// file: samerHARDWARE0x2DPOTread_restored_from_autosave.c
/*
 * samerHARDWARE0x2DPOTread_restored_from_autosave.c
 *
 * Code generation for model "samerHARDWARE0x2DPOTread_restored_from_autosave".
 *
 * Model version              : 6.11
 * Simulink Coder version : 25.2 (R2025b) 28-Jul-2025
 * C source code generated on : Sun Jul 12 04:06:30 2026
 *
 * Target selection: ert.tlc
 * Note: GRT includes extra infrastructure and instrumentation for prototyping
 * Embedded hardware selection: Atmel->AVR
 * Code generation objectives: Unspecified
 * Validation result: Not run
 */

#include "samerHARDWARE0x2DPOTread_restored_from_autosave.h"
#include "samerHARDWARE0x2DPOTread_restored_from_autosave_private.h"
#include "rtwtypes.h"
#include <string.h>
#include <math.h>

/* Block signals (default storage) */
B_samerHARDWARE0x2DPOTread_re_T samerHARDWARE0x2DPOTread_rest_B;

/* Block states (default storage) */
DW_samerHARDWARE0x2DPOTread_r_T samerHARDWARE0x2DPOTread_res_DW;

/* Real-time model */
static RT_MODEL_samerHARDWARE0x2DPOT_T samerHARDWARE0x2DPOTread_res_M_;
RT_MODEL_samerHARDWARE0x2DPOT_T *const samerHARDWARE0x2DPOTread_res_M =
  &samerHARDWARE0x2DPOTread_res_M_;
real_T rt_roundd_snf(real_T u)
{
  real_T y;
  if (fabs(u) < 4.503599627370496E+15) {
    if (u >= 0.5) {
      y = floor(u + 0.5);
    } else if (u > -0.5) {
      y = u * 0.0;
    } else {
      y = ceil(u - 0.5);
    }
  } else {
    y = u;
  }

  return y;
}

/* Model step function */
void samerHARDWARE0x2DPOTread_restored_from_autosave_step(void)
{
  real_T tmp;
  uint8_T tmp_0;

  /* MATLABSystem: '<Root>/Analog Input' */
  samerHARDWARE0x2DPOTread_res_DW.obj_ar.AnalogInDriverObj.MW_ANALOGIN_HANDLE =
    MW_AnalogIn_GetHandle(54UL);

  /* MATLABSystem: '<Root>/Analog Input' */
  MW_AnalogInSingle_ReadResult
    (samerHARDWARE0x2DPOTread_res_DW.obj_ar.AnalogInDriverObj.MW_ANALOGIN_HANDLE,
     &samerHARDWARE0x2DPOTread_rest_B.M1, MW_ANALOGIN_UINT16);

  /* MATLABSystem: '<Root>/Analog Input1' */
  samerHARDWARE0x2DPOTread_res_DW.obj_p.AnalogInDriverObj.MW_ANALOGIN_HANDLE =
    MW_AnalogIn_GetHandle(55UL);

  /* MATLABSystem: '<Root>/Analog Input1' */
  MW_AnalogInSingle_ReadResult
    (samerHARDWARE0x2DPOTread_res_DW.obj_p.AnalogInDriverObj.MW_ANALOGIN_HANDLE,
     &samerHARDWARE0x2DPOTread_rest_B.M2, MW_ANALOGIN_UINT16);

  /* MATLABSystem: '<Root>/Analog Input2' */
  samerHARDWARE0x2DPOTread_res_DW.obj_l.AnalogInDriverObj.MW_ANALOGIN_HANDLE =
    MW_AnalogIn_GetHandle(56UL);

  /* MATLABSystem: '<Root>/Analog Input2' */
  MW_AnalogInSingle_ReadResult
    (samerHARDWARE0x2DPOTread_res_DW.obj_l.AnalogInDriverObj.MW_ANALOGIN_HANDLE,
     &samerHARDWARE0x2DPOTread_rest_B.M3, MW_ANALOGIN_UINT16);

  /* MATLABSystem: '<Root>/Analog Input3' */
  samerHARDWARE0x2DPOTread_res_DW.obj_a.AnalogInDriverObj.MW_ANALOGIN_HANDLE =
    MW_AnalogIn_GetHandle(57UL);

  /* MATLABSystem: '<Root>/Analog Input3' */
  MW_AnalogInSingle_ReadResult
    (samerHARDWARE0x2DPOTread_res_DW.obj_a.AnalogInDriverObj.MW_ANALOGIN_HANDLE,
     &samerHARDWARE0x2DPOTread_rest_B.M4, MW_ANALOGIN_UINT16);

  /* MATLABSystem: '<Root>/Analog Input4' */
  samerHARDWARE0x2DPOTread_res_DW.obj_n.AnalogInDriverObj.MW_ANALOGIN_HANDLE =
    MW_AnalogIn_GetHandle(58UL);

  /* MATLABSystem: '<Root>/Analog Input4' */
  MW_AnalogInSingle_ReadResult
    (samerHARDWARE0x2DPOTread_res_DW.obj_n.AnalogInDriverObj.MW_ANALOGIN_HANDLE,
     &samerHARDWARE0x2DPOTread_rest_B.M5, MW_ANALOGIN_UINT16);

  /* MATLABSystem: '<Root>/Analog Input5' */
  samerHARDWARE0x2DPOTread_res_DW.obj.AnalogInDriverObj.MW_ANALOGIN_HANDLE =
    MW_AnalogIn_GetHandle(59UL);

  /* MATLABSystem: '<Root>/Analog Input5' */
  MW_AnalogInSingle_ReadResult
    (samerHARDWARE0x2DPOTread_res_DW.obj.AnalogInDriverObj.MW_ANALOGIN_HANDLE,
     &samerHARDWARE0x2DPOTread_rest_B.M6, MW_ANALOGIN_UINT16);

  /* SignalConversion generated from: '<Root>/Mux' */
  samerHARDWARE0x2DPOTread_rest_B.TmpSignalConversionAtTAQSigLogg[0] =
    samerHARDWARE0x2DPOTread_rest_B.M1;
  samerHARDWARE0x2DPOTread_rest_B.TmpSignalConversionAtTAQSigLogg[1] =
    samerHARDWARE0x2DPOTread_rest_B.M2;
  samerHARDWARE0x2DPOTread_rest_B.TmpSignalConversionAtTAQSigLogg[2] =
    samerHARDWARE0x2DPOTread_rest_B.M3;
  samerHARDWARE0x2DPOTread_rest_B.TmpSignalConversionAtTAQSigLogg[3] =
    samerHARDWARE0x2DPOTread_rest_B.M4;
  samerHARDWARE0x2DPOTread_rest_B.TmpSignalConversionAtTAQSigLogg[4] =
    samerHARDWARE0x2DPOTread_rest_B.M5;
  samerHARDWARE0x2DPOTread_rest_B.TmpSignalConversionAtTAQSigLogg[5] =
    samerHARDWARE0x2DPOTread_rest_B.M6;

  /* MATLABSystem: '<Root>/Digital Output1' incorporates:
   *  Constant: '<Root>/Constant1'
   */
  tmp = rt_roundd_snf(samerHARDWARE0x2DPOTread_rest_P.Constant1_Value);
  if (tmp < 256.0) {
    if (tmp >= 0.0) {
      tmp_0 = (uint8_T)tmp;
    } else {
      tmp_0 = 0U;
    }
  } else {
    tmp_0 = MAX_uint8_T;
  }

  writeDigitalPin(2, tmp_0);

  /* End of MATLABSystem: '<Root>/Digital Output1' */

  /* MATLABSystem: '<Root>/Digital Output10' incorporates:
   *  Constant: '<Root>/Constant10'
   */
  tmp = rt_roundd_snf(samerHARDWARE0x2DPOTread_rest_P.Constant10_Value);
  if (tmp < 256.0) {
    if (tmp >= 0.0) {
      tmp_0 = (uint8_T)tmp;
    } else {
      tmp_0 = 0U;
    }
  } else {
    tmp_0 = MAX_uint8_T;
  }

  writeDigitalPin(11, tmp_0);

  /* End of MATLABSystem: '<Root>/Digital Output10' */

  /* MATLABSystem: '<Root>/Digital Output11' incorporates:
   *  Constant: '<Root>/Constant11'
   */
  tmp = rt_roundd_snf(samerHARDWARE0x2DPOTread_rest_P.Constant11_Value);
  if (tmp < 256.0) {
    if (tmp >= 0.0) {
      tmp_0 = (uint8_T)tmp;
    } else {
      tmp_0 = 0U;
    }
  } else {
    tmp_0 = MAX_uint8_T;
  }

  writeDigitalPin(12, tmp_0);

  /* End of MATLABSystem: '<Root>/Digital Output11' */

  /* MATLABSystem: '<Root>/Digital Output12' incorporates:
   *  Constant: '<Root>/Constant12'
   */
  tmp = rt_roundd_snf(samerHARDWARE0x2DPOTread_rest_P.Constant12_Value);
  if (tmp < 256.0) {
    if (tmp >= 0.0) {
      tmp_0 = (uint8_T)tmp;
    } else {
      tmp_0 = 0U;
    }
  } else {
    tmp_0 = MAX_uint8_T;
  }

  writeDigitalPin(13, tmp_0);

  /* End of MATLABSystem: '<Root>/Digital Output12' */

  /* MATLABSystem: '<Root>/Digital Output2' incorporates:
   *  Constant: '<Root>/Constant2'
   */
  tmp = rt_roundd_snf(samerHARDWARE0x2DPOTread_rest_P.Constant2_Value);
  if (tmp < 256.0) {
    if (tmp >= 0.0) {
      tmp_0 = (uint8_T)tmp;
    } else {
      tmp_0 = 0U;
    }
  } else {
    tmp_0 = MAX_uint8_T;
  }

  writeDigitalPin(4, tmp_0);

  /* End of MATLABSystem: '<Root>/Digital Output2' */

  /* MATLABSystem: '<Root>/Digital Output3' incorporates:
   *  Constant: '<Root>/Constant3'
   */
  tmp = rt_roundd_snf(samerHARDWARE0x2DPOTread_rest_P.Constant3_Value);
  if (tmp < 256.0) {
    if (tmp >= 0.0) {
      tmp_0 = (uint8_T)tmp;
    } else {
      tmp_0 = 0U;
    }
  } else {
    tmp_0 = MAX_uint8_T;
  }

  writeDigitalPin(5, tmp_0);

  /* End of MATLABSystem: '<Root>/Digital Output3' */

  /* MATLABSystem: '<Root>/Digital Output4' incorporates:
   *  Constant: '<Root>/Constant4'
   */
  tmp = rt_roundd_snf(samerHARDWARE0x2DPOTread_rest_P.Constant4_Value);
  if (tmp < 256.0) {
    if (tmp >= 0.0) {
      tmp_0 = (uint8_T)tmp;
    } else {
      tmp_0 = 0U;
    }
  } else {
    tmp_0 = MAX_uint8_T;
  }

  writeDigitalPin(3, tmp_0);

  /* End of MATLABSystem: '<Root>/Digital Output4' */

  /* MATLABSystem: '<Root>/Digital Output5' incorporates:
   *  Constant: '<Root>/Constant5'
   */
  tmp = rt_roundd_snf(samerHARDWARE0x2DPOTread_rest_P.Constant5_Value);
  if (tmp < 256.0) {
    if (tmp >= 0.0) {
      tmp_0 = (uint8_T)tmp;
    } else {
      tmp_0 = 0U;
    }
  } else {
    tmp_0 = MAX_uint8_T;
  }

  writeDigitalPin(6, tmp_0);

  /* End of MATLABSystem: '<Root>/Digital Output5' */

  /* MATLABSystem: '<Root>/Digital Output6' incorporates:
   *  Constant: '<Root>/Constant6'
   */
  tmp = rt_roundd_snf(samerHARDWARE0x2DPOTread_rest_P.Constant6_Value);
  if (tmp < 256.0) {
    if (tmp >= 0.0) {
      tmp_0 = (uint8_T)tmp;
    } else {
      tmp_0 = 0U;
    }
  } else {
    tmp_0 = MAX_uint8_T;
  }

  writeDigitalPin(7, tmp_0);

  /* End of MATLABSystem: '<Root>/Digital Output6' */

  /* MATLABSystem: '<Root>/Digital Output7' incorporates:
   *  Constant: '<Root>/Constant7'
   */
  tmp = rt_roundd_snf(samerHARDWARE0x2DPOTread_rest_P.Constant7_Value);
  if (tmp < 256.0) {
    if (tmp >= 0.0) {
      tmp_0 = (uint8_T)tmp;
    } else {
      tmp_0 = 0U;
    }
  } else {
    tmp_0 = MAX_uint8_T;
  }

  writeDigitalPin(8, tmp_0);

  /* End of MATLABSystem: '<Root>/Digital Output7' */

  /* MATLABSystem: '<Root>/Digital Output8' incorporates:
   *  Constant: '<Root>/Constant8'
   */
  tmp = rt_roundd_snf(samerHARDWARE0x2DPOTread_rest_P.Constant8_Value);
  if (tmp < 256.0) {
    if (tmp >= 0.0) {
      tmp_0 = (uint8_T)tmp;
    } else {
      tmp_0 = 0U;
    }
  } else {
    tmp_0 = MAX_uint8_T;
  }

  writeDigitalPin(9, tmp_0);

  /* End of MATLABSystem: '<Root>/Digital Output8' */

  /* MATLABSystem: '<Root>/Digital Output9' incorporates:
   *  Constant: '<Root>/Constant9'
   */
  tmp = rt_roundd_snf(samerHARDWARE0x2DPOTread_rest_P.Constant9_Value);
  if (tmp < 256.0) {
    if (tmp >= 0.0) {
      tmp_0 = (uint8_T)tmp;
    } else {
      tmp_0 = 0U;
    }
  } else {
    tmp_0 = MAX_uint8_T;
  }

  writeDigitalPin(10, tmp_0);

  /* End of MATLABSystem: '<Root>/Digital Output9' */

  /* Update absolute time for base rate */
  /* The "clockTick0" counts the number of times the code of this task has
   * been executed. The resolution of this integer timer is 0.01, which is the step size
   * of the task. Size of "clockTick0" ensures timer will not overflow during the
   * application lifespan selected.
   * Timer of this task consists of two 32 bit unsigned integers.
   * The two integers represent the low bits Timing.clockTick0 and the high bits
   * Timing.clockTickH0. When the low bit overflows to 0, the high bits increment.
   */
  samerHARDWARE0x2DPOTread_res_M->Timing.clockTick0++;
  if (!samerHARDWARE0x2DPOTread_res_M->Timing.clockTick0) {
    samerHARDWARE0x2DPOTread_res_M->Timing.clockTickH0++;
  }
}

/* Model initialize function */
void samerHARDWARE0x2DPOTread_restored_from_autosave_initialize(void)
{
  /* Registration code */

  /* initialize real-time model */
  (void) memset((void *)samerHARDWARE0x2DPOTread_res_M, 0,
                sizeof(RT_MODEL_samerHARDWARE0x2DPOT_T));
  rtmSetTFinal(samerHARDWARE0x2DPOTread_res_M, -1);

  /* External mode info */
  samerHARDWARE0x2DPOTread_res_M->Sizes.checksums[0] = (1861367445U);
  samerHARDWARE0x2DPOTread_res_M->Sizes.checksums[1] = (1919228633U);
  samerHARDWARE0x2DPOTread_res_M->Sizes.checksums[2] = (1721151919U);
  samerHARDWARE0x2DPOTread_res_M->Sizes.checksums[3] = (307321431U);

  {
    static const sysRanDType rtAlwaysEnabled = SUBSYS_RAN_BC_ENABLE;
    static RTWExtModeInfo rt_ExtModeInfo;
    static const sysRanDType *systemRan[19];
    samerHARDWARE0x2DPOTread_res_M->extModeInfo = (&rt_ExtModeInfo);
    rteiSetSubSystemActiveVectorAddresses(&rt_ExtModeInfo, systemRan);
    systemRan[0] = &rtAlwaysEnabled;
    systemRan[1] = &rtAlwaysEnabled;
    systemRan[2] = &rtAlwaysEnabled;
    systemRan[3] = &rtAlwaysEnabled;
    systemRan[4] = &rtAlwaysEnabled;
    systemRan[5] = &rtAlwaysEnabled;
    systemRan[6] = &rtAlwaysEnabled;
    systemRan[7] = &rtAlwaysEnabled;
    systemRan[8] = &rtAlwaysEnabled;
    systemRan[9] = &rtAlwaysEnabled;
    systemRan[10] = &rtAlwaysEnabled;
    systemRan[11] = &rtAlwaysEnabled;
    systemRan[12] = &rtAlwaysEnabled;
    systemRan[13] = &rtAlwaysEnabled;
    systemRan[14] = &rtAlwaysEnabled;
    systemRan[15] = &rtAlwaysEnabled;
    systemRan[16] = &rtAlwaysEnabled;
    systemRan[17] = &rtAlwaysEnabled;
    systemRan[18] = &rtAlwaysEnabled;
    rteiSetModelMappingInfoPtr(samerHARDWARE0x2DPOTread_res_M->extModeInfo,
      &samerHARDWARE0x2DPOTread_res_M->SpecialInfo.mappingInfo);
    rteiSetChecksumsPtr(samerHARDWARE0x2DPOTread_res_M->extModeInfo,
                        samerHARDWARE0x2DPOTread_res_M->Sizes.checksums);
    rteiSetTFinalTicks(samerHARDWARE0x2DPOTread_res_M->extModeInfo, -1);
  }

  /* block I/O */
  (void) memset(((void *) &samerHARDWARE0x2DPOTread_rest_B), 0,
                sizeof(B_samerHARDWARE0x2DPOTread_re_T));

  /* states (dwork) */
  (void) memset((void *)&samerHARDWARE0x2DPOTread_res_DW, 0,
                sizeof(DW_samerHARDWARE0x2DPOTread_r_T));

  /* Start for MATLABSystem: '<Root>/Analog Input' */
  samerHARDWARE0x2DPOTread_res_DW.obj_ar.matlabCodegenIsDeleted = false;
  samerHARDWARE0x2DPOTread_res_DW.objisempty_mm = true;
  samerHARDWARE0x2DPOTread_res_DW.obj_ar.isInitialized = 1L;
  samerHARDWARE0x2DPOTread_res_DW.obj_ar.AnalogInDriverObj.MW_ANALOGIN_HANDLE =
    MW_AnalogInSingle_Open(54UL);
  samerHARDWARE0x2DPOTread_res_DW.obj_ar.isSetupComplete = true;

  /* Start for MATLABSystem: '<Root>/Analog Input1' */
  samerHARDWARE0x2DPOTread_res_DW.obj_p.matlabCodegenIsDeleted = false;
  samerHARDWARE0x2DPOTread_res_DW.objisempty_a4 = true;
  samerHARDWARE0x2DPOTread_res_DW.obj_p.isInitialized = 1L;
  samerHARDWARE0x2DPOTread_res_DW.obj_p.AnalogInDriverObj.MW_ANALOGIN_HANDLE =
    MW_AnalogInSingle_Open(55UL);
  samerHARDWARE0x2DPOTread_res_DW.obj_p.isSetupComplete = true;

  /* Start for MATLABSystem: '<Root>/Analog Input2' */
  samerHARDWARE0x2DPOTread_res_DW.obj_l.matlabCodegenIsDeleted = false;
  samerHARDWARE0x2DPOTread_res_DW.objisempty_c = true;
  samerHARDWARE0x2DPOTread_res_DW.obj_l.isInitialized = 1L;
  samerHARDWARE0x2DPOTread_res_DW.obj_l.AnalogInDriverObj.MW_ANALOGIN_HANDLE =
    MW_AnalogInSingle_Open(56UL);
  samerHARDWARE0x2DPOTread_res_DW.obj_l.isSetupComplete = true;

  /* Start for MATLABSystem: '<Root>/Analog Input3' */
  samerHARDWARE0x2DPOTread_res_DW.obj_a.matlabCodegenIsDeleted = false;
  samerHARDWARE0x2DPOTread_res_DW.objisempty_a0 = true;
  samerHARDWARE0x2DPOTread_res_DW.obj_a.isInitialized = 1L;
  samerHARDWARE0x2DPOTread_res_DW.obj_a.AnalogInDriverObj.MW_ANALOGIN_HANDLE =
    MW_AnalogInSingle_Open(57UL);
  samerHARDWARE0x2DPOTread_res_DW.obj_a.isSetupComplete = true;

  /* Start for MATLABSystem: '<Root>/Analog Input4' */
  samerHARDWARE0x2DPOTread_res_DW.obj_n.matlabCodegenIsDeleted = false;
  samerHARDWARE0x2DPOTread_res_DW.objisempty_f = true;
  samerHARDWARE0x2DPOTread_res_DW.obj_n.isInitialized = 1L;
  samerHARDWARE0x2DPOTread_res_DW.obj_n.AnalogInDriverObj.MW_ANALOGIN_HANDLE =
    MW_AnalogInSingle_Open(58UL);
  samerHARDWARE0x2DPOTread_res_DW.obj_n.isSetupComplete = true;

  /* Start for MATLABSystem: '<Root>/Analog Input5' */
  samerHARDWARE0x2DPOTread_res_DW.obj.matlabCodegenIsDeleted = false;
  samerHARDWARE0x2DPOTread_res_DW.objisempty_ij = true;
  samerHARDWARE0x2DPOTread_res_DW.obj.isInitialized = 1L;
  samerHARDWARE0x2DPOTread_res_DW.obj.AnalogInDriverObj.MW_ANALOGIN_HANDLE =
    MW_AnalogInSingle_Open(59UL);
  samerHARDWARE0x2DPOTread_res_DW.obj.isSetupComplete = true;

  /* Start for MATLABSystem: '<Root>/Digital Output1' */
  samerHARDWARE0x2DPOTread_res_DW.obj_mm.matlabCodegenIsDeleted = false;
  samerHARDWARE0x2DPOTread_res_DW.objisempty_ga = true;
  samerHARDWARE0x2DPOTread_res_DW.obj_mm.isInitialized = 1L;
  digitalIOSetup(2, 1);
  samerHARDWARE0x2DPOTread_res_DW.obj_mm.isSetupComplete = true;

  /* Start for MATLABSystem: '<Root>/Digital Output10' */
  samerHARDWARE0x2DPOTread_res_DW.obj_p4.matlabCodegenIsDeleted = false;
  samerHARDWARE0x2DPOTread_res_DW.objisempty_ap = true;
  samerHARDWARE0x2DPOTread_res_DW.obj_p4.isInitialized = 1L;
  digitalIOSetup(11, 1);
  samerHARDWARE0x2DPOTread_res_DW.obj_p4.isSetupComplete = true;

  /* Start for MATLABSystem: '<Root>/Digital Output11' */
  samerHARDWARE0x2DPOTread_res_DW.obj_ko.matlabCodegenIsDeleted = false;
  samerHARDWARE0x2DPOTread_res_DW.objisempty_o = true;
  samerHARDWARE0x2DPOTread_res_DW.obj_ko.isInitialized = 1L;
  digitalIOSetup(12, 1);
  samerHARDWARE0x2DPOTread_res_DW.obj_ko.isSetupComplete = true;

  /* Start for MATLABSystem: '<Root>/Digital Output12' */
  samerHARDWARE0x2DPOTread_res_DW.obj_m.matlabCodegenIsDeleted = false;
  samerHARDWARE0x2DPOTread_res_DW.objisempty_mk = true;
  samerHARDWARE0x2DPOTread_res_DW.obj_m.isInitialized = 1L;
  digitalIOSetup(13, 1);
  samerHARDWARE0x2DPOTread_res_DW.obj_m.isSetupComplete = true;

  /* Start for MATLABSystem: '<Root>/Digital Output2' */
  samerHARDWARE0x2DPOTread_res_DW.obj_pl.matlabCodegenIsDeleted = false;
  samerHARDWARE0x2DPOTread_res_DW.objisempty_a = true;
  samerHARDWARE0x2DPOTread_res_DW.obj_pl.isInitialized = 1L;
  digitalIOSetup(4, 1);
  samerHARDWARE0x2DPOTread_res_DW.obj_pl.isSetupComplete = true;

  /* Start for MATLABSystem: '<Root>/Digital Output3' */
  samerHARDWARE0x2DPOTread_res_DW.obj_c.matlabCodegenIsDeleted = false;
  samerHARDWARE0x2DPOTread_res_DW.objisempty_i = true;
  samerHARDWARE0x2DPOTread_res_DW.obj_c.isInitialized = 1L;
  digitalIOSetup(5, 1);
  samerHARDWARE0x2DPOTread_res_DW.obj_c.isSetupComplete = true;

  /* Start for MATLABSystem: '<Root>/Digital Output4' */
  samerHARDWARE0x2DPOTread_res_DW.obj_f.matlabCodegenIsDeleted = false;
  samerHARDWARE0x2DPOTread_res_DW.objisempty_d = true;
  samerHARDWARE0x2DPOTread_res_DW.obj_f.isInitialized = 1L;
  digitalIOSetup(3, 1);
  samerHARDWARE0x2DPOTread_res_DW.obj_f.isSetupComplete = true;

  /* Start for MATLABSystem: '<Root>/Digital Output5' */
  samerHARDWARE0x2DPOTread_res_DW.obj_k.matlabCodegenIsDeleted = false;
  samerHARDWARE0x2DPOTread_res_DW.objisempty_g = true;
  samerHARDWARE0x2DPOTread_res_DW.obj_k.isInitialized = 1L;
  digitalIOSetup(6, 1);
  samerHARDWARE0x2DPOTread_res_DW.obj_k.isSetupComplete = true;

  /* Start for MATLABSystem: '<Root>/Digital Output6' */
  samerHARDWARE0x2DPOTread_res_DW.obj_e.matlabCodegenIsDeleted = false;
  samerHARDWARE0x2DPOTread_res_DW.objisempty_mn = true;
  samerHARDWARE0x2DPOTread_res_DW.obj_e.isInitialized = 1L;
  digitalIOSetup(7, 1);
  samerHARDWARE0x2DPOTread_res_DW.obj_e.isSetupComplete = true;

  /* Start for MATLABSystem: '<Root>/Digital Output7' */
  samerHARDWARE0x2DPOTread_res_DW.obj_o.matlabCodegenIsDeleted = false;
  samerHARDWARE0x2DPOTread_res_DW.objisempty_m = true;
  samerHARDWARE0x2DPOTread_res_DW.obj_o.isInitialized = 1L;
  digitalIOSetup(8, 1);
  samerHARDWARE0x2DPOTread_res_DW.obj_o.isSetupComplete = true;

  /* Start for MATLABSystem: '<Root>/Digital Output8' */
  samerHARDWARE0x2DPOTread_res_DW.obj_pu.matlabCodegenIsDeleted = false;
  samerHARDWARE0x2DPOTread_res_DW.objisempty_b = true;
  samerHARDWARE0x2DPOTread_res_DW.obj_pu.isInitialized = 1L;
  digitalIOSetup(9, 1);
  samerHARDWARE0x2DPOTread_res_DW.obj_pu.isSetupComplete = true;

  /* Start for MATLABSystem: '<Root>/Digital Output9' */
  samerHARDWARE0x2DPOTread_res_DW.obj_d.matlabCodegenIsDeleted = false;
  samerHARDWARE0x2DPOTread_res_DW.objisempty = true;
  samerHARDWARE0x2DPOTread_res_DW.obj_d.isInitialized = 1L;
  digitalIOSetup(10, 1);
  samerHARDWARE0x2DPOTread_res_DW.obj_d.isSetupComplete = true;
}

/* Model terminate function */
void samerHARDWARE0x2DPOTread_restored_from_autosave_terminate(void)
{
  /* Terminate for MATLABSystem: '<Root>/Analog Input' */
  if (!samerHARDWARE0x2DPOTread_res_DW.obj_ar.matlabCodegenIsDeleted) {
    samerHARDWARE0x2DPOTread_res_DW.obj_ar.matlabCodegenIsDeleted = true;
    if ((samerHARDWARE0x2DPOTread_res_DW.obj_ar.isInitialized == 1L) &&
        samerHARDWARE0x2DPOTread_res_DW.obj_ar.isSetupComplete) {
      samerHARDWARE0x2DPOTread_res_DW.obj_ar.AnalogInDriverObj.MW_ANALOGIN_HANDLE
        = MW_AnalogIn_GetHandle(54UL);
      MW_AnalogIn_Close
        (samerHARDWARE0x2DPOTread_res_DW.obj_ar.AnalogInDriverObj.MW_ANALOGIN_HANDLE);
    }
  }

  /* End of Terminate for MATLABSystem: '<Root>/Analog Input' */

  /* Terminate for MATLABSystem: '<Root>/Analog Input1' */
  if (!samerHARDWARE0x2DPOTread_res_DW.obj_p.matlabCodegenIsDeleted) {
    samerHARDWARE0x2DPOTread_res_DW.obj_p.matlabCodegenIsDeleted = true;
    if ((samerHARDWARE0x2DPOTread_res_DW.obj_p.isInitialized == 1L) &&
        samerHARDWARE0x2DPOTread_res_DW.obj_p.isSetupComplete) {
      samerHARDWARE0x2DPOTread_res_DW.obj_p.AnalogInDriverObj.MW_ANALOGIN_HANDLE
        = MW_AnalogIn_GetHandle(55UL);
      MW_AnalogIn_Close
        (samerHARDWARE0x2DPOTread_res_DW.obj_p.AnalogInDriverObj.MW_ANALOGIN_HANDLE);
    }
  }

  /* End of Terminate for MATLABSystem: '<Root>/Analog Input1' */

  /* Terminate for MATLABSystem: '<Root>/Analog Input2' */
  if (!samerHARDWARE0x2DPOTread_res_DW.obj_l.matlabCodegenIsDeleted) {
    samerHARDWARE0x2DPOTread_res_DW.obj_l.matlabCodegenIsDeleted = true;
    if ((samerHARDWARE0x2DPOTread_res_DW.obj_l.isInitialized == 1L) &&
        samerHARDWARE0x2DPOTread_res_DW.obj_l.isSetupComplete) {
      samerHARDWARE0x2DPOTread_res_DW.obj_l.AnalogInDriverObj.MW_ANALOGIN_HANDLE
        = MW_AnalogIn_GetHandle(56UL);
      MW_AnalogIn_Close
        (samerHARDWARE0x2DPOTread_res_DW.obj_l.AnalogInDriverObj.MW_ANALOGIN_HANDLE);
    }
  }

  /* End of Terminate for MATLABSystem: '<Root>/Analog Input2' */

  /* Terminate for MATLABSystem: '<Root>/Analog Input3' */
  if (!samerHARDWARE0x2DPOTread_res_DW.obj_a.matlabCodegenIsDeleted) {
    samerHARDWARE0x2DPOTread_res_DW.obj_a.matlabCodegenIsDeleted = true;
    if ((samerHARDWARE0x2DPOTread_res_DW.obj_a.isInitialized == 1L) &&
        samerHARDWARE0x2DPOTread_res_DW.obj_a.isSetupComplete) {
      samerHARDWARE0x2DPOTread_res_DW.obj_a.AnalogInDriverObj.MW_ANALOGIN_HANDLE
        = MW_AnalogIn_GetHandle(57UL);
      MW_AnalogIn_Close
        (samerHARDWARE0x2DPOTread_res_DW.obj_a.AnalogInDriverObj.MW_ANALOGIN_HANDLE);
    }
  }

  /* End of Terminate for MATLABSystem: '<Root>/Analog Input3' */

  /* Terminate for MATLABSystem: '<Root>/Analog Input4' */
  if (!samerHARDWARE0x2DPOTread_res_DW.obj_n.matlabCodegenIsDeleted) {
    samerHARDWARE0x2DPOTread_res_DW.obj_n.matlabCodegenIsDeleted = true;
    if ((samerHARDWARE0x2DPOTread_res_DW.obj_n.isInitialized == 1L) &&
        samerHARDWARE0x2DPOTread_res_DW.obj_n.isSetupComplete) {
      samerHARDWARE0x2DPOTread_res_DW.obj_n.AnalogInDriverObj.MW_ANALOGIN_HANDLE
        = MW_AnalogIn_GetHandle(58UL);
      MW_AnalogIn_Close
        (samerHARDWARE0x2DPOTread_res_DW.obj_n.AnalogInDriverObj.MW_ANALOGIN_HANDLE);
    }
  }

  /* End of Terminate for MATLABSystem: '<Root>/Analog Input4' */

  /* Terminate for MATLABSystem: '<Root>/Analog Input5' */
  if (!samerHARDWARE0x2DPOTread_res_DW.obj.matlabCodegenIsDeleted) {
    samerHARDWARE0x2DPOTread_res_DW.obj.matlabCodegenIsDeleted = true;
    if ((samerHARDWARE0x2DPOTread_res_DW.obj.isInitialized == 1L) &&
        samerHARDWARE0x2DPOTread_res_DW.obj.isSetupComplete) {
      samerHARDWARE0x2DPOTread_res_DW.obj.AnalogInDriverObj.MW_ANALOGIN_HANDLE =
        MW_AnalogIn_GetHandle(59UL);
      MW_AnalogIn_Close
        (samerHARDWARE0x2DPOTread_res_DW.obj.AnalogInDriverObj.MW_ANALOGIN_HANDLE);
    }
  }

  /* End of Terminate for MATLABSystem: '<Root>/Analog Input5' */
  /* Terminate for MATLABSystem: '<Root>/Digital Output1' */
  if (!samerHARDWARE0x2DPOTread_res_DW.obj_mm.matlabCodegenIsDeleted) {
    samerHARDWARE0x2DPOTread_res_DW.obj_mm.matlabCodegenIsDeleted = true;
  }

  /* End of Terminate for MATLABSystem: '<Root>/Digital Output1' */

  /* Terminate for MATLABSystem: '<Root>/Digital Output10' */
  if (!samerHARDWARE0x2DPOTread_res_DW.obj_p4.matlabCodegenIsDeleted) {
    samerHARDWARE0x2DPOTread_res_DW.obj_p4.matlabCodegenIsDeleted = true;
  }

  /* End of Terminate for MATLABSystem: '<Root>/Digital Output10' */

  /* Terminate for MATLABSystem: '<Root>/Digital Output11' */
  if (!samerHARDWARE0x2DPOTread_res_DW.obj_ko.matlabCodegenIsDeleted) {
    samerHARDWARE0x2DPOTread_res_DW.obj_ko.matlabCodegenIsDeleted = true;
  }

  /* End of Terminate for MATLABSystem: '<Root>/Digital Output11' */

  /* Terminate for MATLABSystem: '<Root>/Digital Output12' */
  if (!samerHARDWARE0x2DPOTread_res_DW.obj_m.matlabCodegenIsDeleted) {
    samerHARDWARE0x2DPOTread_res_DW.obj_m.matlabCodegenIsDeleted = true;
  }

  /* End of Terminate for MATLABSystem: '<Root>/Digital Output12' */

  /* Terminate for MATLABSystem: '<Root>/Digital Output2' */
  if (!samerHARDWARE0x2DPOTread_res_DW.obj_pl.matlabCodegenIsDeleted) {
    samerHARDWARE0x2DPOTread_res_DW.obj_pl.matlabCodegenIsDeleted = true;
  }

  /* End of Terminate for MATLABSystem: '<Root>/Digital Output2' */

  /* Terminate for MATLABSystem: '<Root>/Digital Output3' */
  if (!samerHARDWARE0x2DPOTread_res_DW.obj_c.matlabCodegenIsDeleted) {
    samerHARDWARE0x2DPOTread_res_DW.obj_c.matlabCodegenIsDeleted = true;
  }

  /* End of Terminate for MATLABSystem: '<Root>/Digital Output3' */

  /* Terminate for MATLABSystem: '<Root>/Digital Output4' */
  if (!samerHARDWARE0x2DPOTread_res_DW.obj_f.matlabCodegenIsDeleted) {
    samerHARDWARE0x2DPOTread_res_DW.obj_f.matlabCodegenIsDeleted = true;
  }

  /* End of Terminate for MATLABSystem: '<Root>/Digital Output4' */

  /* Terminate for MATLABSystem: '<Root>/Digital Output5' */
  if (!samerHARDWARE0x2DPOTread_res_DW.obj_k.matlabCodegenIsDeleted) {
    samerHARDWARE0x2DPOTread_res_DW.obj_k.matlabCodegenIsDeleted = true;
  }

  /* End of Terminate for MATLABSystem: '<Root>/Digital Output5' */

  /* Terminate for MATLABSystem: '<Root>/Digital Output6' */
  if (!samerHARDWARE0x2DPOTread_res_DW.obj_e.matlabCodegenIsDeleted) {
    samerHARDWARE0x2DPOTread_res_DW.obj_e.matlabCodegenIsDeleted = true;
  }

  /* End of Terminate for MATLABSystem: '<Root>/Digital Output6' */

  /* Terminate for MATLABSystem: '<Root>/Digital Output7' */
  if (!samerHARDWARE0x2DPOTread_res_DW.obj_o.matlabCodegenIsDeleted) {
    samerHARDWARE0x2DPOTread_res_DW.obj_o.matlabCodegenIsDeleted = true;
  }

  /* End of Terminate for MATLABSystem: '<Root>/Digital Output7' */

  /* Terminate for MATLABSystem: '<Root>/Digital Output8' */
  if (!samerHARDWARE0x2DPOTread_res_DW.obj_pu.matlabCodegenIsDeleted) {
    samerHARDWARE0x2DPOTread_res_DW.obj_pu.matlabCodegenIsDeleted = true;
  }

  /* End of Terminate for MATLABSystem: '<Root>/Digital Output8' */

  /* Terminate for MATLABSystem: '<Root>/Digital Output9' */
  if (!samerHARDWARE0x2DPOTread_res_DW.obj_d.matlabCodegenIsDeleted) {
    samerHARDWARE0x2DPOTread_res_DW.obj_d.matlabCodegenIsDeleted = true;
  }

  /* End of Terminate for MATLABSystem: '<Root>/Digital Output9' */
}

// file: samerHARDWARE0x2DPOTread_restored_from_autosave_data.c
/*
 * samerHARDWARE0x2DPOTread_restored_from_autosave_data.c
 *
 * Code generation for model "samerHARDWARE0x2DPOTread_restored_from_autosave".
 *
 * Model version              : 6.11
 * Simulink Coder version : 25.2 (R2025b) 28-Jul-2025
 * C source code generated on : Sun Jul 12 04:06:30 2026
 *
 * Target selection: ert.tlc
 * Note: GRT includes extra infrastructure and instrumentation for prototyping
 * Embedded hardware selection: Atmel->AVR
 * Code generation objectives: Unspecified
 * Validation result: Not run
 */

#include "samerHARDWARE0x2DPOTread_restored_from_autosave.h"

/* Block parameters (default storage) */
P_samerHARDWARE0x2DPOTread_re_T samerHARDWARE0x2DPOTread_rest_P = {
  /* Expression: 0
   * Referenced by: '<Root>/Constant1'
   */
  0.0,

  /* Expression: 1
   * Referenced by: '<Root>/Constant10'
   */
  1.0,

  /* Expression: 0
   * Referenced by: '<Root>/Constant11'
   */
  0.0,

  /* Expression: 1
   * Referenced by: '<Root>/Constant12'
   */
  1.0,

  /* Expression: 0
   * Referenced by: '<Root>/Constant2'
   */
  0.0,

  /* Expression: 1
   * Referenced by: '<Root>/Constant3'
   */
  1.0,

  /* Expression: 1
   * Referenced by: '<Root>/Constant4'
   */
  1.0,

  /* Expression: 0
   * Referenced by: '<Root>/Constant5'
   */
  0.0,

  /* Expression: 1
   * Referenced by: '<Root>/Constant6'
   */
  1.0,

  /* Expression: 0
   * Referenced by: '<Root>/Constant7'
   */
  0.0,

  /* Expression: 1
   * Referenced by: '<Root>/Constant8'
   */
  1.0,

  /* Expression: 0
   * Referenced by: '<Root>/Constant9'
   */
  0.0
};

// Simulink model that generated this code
simulink model "samerHARDWARE0x2DPOTread_restored_from_autosave"  (R2025b)
settings: Solver=FixedStepDiscrete  StartTime=0.0  StopTime=inf  RelTol=1e-3  EnableMultiTasking=on
libraries: arduinolib x18

== system samerHARDWARE0x2DPOTread_restored_from_autosave ==
  Analog Input : arduinolib/Analog Input  pinNumber=0  ReadResultsOnly=off  ConversionTriggerSource=Software  ExternalTriggerType=uint32( 0 )  OutputDataType=uint16  EnableConversionCompleteNotify=off  EnableOuputStatus=off  SampleTime=0.01  blockPlatform=arduino
  Analog Input1 : arduinolib/Analog Input  pinNumber=1  ReadResultsOnly=off  ConversionTriggerSource=Software  ExternalTriggerType=uint32( 0 )  OutputDataType=uint16  EnableConversionCompleteNotify=off  EnableOuputStatus=off  SampleTime=0.01  blockPlatform=arduino
  Analog Input2 : arduinolib/Analog Input  pinNumber=2  ReadResultsOnly=off  ConversionTriggerSource=Software  ExternalTriggerType=uint32( 0 )  OutputDataType=uint16  EnableConversionCompleteNotify=off  EnableOuputStatus=off  SampleTime=0.01  blockPlatform=arduino
  Analog Input3 : arduinolib/Analog Input  pinNumber=3  ReadResultsOnly=off  ConversionTriggerSource=Software  ExternalTriggerType=uint32( 0 )  OutputDataType=uint16  EnableConversionCompleteNotify=off  EnableOuputStatus=off  SampleTime=0.01  blockPlatform=arduino
  Analog Input4 : arduinolib/Analog Input  pinNumber=4  ReadResultsOnly=off  ConversionTriggerSource=Software  ExternalTriggerType=uint32( 0 )  OutputDataType=uint16  EnableConversionCompleteNotify=off  EnableOuputStatus=off  SampleTime=0.01  blockPlatform=arduino
  Analog Input5 : arduinolib/Analog Input  pinNumber=5  ReadResultsOnly=off  ConversionTriggerSource=Software  ExternalTriggerType=uint32( 0 )  OutputDataType=uint16  EnableConversionCompleteNotify=off  EnableOuputStatus=off  SampleTime=0.01  blockPlatform=arduino
  Constant{1..2,5,7,9,11} (6 alike) : Constant  Value=0
  Constant{3..4,6,8,10,12} (6 alike) : Constant
  Digital Output1 : arduinolib/Digital Output  pinNumber=2  Direction=output  blockPlatform=arduino
  Digital Output10 : arduinolib/Digital Output  pinNumber=11  Direction=output  blockPlatform=arduino
  Digital Output11 : arduinolib/Digital Output  pinNumber=12  Direction=output  blockPlatform=arduino
  Digital Output12 : arduinolib/Digital Output  pinNumber=13  Direction=output  blockPlatform=arduino
  Digital Output2 : arduinolib/Digital Output  pinNumber=4  Direction=output  blockPlatform=arduino
  Digital Output3 : arduinolib/Digital Output  pinNumber=5  Direction=output  blockPlatform=arduino
  Digital Output4 : arduinolib/Digital Output  pinNumber=3  Direction=output  blockPlatform=arduino
  Digital Output5 : arduinolib/Digital Output  pinNumber=6  Direction=output  blockPlatform=arduino
  Digital Output6 : arduinolib/Digital Output  pinNumber=7  Direction=output  blockPlatform=arduino
  Digital Output7 : arduinolib/Digital Output  pinNumber=8  Direction=output  blockPlatform=arduino
  Digital Output8 : arduinolib/Digital Output  pinNumber=9  Direction=output  blockPlatform=arduino
  Digital Output9 : arduinolib/Digital Output  pinNumber=10  Direction=output  blockPlatform=arduino
  Mux : Mux  Inputs=6
  Scope : Scope
  wires:
  Analog Input/1 -> Mux/1  "M1"
  Analog Input1/1 -> Mux/2  "M2"
  Analog Input2/1 -> Mux/3  "M3"
  Analog Input3/1 -> Mux/4  "M4"
  Analog Input4/1 -> Mux/5  "M5"
  Analog Input5/1 -> Mux/6  "M6"
  Mux/1 -> Scope/1
  Constant2/1 -> Digital Output2/1
  Constant3/1 -> Digital Output3/1
  Constant4/1 -> Digital Output4/1
  Constant1/1 -> Digital Output1/1
  Constant6/1 -> Digital Output6/1
  Constant5/1 -> Digital Output5/1
  Constant8/1 -> Digital Output8/1
  Constant7/1 -> Digital Output7/1
  Constant10/1 -> Digital Output10/1
  Constant9/1 -> Digital Output9/1
  Constant12/1 -> Digital Output12/1
  Constant11/1 -> Digital Output11/1
